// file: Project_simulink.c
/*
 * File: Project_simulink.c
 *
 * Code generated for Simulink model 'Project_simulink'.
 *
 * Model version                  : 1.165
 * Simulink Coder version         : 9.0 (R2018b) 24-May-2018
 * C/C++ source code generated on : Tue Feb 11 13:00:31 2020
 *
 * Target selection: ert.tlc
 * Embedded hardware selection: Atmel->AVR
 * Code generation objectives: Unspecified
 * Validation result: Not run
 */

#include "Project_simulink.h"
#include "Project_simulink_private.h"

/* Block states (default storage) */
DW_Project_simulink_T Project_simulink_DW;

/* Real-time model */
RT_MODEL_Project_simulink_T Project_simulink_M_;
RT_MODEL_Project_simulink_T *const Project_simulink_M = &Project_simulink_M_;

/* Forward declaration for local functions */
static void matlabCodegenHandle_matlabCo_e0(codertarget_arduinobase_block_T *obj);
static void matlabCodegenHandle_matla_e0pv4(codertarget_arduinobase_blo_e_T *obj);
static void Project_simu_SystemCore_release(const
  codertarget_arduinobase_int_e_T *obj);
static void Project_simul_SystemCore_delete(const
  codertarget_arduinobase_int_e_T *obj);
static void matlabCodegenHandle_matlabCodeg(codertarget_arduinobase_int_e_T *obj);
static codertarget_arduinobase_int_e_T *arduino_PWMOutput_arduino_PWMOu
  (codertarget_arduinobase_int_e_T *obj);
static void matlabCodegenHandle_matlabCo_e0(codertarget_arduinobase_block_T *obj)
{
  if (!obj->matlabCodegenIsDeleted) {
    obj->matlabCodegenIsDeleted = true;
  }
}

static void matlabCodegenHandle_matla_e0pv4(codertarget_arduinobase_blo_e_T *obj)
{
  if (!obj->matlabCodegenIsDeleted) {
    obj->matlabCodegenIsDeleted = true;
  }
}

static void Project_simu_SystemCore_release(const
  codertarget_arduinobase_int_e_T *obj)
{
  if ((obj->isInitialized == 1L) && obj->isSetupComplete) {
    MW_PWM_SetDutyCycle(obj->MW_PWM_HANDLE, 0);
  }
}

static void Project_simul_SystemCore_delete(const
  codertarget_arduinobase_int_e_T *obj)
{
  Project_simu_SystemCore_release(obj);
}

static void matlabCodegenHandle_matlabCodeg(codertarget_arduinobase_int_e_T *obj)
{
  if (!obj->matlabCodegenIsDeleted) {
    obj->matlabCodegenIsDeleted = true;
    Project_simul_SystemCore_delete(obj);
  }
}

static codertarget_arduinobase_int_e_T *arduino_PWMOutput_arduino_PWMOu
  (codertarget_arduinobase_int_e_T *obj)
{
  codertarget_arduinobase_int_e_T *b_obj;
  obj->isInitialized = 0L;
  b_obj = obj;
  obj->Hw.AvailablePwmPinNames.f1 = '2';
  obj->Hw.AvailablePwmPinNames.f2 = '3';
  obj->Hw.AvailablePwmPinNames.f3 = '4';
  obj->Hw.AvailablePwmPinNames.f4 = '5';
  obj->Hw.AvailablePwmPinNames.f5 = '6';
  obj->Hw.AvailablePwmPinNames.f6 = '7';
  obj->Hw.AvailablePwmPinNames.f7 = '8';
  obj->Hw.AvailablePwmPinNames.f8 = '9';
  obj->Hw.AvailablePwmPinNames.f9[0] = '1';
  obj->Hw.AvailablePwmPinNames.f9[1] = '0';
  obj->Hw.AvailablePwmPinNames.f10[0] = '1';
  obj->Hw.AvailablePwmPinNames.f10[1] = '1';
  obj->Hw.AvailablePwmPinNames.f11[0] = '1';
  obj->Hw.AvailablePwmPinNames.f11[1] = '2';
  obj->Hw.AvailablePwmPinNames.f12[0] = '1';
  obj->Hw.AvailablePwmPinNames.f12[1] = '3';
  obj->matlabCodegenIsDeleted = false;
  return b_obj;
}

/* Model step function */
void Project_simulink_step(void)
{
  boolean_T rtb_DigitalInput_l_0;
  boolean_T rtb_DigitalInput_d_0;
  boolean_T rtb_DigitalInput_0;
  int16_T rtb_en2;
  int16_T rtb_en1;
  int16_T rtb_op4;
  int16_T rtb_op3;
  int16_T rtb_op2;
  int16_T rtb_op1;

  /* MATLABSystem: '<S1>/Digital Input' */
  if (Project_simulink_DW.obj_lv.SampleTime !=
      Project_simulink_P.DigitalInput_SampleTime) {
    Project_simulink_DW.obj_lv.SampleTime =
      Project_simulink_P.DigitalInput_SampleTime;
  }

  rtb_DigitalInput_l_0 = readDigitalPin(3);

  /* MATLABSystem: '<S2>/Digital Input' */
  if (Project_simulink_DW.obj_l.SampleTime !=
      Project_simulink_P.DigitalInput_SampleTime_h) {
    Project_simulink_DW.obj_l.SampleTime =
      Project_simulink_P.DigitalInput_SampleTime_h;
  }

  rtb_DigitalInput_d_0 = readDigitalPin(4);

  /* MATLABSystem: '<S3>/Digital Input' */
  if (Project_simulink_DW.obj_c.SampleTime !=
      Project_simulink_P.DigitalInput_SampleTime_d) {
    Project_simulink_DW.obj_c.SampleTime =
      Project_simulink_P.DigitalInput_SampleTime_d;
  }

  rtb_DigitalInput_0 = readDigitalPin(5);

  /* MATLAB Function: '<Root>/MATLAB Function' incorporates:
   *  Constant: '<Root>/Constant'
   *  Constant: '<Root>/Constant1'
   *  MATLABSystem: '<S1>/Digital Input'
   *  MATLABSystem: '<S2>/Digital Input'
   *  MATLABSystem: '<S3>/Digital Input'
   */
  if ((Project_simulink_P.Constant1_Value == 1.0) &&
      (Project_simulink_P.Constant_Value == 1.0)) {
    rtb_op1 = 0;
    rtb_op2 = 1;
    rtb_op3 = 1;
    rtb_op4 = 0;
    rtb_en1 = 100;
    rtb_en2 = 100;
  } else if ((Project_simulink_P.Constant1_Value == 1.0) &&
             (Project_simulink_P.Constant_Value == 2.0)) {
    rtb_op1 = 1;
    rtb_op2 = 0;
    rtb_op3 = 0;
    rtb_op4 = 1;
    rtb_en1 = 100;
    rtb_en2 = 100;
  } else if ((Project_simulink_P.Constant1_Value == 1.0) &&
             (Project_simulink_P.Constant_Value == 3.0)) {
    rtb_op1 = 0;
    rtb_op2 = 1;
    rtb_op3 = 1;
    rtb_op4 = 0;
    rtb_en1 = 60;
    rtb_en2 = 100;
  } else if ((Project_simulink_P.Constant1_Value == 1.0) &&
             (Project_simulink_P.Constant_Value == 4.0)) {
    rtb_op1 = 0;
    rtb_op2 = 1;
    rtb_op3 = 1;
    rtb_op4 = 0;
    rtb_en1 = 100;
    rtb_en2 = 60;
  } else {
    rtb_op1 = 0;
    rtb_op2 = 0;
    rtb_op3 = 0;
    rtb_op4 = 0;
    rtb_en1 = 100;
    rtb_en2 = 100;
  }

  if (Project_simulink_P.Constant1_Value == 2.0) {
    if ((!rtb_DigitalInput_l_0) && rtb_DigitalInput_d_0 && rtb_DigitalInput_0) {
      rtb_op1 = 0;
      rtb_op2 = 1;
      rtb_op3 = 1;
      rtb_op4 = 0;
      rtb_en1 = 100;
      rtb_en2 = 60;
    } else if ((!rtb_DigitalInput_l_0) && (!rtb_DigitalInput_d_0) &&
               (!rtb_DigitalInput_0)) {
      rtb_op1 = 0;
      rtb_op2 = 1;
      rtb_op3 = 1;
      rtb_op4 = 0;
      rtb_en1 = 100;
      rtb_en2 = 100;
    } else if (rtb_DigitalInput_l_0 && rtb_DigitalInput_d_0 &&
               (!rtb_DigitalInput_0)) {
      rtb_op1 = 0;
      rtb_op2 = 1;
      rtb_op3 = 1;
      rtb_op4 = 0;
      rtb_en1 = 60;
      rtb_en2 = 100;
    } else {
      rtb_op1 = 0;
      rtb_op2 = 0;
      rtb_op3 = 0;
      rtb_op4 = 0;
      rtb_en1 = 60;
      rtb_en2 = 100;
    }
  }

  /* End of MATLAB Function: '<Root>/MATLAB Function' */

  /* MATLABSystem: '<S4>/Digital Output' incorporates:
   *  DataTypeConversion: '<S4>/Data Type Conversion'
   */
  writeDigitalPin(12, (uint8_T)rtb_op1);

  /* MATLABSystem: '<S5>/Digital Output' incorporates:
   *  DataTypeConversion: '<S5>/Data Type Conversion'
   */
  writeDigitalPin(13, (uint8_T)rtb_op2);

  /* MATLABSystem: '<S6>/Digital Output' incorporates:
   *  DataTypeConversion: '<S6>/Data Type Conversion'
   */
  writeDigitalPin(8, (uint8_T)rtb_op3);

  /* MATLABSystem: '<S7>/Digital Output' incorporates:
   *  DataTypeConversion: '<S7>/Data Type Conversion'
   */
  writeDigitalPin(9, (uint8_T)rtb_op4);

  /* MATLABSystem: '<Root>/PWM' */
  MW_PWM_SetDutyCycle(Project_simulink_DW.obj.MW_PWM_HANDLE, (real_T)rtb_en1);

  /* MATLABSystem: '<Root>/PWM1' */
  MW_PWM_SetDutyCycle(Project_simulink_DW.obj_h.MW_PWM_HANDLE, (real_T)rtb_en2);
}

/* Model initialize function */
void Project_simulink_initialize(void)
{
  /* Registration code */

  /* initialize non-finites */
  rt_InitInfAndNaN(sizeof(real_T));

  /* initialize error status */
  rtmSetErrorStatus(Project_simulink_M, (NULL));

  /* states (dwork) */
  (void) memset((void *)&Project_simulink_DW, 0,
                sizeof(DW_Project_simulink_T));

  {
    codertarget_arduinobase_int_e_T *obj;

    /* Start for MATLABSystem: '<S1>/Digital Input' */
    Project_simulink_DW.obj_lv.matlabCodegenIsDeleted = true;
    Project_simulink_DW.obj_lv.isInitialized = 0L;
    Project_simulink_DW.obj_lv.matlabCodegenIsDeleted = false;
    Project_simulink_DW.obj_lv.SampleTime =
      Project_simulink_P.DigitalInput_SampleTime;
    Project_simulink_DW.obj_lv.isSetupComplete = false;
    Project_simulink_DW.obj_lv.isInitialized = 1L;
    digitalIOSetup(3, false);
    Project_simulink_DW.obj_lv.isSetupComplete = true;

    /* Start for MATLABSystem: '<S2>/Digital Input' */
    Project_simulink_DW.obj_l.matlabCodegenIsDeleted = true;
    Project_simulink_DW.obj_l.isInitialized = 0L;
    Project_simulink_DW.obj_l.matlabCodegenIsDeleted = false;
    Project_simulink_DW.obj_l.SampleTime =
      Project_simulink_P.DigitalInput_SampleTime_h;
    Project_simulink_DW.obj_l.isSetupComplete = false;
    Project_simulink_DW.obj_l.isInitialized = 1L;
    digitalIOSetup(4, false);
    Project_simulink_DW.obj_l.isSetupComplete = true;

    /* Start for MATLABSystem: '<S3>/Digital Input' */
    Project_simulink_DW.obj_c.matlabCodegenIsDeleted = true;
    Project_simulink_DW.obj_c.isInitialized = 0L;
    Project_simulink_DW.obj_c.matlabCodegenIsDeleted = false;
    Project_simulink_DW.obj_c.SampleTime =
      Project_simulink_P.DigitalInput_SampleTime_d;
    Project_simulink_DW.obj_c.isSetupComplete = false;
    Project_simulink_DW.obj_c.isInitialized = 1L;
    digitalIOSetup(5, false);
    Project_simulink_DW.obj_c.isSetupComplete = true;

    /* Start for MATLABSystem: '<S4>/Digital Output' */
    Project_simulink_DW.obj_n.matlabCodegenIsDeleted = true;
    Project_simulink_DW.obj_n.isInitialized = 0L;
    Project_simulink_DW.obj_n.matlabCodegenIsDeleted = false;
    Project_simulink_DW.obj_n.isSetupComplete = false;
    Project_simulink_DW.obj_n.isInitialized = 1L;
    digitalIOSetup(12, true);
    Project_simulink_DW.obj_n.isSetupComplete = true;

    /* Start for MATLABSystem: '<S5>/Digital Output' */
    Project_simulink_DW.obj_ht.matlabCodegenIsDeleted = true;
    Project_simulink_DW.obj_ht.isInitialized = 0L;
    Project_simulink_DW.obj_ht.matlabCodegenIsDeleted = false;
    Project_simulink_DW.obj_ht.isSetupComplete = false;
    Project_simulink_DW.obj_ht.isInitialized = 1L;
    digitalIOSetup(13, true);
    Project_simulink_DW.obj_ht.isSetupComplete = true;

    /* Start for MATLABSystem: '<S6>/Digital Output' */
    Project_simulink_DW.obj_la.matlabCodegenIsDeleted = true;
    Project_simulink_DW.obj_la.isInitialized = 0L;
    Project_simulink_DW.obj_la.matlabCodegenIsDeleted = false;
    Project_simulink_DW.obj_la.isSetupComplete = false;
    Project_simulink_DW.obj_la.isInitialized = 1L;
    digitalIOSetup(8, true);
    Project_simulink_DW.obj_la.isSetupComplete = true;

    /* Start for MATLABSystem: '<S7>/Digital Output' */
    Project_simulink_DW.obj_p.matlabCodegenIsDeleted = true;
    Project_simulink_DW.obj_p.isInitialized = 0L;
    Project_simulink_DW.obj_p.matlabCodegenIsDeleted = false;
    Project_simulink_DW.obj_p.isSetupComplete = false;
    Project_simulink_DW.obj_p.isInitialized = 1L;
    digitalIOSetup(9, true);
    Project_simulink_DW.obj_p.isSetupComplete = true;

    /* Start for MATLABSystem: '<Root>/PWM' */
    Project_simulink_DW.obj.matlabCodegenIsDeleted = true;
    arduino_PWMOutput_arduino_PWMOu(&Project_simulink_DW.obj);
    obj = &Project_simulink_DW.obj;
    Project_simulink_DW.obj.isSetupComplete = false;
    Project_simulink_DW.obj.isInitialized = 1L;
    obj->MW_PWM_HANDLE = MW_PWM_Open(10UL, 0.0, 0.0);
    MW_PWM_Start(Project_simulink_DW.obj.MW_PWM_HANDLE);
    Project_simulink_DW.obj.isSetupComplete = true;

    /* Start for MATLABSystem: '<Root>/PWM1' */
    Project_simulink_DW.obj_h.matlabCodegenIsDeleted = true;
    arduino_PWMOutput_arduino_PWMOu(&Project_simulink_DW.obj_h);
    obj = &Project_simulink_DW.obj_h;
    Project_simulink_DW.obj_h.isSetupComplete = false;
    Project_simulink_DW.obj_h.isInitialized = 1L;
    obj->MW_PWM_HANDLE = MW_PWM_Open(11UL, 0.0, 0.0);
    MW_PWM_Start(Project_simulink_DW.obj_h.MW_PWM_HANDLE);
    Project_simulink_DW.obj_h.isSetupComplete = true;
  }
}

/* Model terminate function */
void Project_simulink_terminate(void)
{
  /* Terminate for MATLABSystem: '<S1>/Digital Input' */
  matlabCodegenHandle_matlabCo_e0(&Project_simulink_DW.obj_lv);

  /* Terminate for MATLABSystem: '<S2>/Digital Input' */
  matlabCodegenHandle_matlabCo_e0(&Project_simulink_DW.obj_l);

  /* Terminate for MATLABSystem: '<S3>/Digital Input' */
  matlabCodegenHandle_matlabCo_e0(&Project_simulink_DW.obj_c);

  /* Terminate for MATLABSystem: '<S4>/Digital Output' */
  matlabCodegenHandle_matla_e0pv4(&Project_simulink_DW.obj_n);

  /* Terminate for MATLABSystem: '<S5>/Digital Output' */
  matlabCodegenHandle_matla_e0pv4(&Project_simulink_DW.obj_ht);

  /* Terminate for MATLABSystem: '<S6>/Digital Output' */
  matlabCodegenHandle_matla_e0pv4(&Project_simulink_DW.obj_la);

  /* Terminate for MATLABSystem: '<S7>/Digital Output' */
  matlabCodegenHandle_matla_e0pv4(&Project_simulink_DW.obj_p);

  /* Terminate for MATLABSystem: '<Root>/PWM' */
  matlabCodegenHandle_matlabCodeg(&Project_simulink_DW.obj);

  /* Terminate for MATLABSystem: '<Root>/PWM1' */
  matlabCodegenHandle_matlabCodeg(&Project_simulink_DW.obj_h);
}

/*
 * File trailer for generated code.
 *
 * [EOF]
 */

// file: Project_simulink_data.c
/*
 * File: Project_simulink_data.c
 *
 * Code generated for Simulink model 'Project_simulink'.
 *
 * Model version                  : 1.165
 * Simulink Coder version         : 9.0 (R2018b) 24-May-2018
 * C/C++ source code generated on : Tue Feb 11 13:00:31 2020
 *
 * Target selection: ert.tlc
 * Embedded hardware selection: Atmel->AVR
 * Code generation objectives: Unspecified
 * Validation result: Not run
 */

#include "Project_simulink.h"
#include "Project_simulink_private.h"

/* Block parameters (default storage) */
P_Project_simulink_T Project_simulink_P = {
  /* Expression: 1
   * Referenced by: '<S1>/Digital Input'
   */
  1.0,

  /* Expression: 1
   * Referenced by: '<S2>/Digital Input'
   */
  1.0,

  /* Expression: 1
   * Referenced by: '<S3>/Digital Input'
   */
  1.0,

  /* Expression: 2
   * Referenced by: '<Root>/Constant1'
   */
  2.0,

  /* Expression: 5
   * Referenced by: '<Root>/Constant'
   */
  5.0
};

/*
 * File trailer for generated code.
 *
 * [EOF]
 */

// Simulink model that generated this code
simulink model "Project_simulink"  (R2018b)
settings: Solver=FixedStepAuto  StartTime=0.0  StopTime=inf  RelTol=1e-3  EnableMultiTasking=on
libraries: arduinolib x9

== system Project_simulink ==
  Constant : Constant  Value=5
  Constant1 : Constant
  Digital Input : arduinolib/Digital Input  pinNumber=3  sampleTime=1  blockPlatform=arduino
  Digital Input1 : arduinolib/Digital Input  pinNumber=4  sampleTime=1  blockPlatform=arduino
  Digital Input2 : arduinolib/Digital Input  pinNumber=5  sampleTime=1  blockPlatform=arduino
  Digital Output : arduinolib/Digital Output  pinNumber=12  blockPlatform=arduino
  Digital Output1 : arduinolib/Digital Output  pinNumber=13  blockPlatform=arduino
  Digital Output2 : arduinolib/Digital Output  pinNumber=8  blockPlatform=arduino
  Digital Output3 : arduinolib/Digital Output  pinNumber=9  blockPlatform=arduino
  MATLAB Function : MATLAB Function  TreatAsAtomicUnit=on
  PWM : arduinolib/PWM  pinNumber=10  EnableInputFrequency=off  InitialFrequency=2000  InitialDutyCycle=0  NotificationType=None  blockPlatform=arduino
  PWM1 : arduinolib/PWM  pinNumber=11  EnableInputFrequency=off  InitialFrequency=2000  InitialDutyCycle=0  NotificationType=None  blockPlatform=arduino
  Scope : Scope  NumInputPorts=2
  Scope1 : Scope  NumInputPorts=3
  wires:
  MATLAB Function/1(op1) -> Digital Output/1
  MATLAB Function/2(op2) -> Digital Output1/1
  MATLAB Function/3(op3) -> Digital Output2/1
  MATLAB Function/4(op4) -> Digital Output3/1
  MATLAB Function/5(en1) -> PWM/1, Scope/1
  MATLAB Function/6(en2) -> PWM1/1, Scope/2
  Constant1/1 -> MATLAB Function/1(ip1)
  Constant/1 -> MATLAB Function/2(ip2)
  Digital Input/1 -> Scope1/1, MATLAB Function/3(sen1)
  Digital Input1/1 -> Scope1/3, MATLAB Function/4(sen2)
  Digital Input2/1 -> Scope1/2, MATLAB Function/5(sen3)

== matlab function Project_simulink/MATLAB Function ==
function [op1,op2,op3,op4,en1,en2] = fcn(ip1,ip2, sen1, sen2, sen3)
        %Manual, Forward Mode
        if (ip1 == 1 && ip2 == 1)
         op1 = 0;
         op2 = 1;
         op3 = 1;
         op4 = 0;
         en1 = 100;
         en2 = 100;
        %Manual, Backward Mode
        elseif (ip1 == 1 && ip2 == 2)
         op1 = 1;
         op2 = 0;
         op3 = 0;
         op4 = 1; 
         en1=100;
         en2=100;
        %Manual, Left Mode
        elseif (ip1 == 1 && ip2 == 3)
         op1 = 0;
         op2 = 1;
         op3 = 1;
         op4 = 0;
         en1=60;
         en2=100;
         %Manual, Right Mode
        elseif (ip1 == 1 && ip2 == 4)
         op1 = 0;
         op2 = 1;
         op3 = 1;
         op4 = 0;
         en1=100;
         en2=60;
        else
         op1 = 0;
         op2 = 0;
         op3 = 0;
         op4 = 0;
         en1 = 100;
         en2 = 100;
        end
         %LineFollower Mode
        if (ip1==2 )
            if (sen1 ==0 && sen2 == 1 && sen3 == 1)
         op1 = 0;
         op2 = 1;
         op3 = 1;
         op4 = 0;
         en1 = 100;
         en2 = 60;
            elseif (sen1 ==0 && sen2 == 0 && sen3 == 0)
         op1 = 0;
         op2 = 1;
         op3 = 1;
         op4 = 0;
         en1 = 100;
         en2 = 100;   
            elseif (sen1 ==1 && sen2 == 1 && sen3 == 0)
         op1 = 0;
         op2 = 1;
         op3 = 1;
         op4 = 0;
         en1 = 60;
         en2 = 100; 
            else 
                             op1 = 0;
         op2 = 0;
         op3 = 0;
         op4 = 0;
         en1 = 60;
         en2 = 100;               
            end
        end
end
